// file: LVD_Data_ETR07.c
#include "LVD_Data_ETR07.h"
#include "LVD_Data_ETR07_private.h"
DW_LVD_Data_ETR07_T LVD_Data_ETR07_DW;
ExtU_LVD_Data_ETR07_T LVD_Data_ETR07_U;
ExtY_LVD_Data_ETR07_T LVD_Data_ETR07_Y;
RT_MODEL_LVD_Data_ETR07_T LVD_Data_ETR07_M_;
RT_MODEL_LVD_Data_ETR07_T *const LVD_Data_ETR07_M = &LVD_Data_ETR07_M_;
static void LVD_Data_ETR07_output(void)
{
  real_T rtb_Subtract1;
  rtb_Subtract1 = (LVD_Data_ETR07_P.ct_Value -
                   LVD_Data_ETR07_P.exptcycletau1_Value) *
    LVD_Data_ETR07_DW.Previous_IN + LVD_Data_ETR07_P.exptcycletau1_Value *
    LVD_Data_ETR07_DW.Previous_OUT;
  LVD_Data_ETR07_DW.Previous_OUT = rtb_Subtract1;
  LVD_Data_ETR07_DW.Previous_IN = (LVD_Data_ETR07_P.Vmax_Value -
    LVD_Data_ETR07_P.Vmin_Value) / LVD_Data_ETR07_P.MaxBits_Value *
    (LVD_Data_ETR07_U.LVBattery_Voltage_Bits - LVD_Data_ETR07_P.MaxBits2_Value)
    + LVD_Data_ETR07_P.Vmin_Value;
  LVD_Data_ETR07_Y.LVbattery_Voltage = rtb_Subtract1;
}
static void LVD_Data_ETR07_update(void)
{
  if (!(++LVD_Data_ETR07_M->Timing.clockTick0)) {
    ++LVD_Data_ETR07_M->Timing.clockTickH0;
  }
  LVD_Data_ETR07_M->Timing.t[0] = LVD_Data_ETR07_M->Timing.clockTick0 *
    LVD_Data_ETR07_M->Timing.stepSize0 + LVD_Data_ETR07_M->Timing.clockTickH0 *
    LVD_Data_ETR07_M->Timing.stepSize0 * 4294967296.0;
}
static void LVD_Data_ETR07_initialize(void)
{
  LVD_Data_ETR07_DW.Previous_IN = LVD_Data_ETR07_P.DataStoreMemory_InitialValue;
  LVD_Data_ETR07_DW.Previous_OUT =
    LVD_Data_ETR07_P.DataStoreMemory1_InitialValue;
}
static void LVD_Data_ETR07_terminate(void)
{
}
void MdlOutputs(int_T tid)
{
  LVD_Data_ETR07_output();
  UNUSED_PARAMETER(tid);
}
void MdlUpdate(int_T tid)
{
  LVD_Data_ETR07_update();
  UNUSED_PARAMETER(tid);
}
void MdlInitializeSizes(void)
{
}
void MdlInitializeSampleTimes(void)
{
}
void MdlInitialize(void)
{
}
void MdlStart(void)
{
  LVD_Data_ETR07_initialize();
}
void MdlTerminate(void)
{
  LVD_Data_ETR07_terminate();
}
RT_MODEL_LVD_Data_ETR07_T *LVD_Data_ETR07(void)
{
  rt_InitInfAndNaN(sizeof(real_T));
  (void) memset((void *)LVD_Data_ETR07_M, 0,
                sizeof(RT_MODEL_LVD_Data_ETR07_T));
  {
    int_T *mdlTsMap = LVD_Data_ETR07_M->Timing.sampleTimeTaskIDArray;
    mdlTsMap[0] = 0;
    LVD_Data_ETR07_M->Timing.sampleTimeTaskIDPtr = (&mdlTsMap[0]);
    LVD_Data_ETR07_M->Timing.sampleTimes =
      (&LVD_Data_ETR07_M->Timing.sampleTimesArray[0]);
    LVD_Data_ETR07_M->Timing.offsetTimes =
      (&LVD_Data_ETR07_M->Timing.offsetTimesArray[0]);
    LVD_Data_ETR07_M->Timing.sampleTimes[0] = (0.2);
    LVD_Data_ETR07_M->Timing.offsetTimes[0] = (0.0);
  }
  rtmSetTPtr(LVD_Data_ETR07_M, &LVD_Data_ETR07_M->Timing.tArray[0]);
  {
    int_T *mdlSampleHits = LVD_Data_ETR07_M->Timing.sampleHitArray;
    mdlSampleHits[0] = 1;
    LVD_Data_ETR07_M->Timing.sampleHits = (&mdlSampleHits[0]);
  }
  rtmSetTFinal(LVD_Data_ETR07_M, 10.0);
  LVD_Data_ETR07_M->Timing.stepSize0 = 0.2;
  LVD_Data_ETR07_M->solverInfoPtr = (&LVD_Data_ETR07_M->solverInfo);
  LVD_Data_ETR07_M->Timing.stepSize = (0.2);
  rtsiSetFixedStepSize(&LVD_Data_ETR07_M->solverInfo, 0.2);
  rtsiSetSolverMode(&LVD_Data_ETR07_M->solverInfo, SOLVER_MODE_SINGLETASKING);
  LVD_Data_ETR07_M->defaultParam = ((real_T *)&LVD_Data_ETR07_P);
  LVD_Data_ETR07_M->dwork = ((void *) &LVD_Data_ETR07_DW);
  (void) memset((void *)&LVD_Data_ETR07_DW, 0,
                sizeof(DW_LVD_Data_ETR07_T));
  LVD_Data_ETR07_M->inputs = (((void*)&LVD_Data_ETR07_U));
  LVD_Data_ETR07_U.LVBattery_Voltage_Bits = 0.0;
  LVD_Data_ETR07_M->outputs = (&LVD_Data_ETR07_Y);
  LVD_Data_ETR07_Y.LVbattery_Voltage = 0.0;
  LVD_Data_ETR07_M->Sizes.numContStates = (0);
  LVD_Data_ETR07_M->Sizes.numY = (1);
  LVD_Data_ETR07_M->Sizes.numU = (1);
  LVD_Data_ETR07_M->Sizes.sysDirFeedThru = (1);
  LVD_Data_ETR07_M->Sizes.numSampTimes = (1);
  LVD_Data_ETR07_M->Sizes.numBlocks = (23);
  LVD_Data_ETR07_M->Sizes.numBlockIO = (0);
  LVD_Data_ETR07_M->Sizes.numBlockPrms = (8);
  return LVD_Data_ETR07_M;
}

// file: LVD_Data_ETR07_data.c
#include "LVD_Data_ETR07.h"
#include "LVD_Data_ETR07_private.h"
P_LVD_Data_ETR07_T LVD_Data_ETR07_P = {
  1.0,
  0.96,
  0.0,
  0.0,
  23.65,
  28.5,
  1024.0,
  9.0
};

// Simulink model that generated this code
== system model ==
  LVBattery_Voltage_Bits : Inport
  LVbattery_Voltage : Outport  <- 1: Subsystem#1
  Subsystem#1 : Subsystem  <- 1: Sum#1
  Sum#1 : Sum  <- 1: Vmin, 2: Product#1
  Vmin : Constant  Value=23.65
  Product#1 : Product  <- 1: Product#2, 2: Sum#2
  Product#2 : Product  Inputs=*/  <- 1: Sum#3, 2: MaxBits
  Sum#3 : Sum  Inputs=-+  <- 1: Vmin, 2: Vmax
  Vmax : Constant  Value=28.5
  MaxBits : Constant  Value=1024
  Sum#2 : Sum  Inputs=+-  <- 1: LVBattery_Voltage_Bits, 2: MaxBits2
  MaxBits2 : Constant  Value=9
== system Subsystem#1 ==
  IN : Inport
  OUT : Outport  <- 1: Subtract1
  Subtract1 : Sum  <- 1: Product#3, 2: Product#4
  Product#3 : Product  <- 1: DataStoreRead#1, 2: Sum#4
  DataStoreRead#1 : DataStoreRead  DataStoreName=Previous_IN
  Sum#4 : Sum  Inputs=+-  <- 1: ct, 2: exptcycletau1
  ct : Constant
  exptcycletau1 : Constant  Value=0.96
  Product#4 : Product  <- 1: exptcycletau1, 2: DataStoreRead#2
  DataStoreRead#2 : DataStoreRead  DataStoreName=Previous_OUT
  DataStoreWrite#1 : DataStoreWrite  DataStoreName=Previous_OUT  <- 1: Subtract1
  DataStoreWrite#2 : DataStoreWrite  DataStoreName=Previous_IN  <- 1: IN
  DataStoreMemory : DataStoreMemory  DataStoreName=Previous_IN
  DataStoreMemory1 : DataStoreMemory  DataStoreName=Previous_OUT
